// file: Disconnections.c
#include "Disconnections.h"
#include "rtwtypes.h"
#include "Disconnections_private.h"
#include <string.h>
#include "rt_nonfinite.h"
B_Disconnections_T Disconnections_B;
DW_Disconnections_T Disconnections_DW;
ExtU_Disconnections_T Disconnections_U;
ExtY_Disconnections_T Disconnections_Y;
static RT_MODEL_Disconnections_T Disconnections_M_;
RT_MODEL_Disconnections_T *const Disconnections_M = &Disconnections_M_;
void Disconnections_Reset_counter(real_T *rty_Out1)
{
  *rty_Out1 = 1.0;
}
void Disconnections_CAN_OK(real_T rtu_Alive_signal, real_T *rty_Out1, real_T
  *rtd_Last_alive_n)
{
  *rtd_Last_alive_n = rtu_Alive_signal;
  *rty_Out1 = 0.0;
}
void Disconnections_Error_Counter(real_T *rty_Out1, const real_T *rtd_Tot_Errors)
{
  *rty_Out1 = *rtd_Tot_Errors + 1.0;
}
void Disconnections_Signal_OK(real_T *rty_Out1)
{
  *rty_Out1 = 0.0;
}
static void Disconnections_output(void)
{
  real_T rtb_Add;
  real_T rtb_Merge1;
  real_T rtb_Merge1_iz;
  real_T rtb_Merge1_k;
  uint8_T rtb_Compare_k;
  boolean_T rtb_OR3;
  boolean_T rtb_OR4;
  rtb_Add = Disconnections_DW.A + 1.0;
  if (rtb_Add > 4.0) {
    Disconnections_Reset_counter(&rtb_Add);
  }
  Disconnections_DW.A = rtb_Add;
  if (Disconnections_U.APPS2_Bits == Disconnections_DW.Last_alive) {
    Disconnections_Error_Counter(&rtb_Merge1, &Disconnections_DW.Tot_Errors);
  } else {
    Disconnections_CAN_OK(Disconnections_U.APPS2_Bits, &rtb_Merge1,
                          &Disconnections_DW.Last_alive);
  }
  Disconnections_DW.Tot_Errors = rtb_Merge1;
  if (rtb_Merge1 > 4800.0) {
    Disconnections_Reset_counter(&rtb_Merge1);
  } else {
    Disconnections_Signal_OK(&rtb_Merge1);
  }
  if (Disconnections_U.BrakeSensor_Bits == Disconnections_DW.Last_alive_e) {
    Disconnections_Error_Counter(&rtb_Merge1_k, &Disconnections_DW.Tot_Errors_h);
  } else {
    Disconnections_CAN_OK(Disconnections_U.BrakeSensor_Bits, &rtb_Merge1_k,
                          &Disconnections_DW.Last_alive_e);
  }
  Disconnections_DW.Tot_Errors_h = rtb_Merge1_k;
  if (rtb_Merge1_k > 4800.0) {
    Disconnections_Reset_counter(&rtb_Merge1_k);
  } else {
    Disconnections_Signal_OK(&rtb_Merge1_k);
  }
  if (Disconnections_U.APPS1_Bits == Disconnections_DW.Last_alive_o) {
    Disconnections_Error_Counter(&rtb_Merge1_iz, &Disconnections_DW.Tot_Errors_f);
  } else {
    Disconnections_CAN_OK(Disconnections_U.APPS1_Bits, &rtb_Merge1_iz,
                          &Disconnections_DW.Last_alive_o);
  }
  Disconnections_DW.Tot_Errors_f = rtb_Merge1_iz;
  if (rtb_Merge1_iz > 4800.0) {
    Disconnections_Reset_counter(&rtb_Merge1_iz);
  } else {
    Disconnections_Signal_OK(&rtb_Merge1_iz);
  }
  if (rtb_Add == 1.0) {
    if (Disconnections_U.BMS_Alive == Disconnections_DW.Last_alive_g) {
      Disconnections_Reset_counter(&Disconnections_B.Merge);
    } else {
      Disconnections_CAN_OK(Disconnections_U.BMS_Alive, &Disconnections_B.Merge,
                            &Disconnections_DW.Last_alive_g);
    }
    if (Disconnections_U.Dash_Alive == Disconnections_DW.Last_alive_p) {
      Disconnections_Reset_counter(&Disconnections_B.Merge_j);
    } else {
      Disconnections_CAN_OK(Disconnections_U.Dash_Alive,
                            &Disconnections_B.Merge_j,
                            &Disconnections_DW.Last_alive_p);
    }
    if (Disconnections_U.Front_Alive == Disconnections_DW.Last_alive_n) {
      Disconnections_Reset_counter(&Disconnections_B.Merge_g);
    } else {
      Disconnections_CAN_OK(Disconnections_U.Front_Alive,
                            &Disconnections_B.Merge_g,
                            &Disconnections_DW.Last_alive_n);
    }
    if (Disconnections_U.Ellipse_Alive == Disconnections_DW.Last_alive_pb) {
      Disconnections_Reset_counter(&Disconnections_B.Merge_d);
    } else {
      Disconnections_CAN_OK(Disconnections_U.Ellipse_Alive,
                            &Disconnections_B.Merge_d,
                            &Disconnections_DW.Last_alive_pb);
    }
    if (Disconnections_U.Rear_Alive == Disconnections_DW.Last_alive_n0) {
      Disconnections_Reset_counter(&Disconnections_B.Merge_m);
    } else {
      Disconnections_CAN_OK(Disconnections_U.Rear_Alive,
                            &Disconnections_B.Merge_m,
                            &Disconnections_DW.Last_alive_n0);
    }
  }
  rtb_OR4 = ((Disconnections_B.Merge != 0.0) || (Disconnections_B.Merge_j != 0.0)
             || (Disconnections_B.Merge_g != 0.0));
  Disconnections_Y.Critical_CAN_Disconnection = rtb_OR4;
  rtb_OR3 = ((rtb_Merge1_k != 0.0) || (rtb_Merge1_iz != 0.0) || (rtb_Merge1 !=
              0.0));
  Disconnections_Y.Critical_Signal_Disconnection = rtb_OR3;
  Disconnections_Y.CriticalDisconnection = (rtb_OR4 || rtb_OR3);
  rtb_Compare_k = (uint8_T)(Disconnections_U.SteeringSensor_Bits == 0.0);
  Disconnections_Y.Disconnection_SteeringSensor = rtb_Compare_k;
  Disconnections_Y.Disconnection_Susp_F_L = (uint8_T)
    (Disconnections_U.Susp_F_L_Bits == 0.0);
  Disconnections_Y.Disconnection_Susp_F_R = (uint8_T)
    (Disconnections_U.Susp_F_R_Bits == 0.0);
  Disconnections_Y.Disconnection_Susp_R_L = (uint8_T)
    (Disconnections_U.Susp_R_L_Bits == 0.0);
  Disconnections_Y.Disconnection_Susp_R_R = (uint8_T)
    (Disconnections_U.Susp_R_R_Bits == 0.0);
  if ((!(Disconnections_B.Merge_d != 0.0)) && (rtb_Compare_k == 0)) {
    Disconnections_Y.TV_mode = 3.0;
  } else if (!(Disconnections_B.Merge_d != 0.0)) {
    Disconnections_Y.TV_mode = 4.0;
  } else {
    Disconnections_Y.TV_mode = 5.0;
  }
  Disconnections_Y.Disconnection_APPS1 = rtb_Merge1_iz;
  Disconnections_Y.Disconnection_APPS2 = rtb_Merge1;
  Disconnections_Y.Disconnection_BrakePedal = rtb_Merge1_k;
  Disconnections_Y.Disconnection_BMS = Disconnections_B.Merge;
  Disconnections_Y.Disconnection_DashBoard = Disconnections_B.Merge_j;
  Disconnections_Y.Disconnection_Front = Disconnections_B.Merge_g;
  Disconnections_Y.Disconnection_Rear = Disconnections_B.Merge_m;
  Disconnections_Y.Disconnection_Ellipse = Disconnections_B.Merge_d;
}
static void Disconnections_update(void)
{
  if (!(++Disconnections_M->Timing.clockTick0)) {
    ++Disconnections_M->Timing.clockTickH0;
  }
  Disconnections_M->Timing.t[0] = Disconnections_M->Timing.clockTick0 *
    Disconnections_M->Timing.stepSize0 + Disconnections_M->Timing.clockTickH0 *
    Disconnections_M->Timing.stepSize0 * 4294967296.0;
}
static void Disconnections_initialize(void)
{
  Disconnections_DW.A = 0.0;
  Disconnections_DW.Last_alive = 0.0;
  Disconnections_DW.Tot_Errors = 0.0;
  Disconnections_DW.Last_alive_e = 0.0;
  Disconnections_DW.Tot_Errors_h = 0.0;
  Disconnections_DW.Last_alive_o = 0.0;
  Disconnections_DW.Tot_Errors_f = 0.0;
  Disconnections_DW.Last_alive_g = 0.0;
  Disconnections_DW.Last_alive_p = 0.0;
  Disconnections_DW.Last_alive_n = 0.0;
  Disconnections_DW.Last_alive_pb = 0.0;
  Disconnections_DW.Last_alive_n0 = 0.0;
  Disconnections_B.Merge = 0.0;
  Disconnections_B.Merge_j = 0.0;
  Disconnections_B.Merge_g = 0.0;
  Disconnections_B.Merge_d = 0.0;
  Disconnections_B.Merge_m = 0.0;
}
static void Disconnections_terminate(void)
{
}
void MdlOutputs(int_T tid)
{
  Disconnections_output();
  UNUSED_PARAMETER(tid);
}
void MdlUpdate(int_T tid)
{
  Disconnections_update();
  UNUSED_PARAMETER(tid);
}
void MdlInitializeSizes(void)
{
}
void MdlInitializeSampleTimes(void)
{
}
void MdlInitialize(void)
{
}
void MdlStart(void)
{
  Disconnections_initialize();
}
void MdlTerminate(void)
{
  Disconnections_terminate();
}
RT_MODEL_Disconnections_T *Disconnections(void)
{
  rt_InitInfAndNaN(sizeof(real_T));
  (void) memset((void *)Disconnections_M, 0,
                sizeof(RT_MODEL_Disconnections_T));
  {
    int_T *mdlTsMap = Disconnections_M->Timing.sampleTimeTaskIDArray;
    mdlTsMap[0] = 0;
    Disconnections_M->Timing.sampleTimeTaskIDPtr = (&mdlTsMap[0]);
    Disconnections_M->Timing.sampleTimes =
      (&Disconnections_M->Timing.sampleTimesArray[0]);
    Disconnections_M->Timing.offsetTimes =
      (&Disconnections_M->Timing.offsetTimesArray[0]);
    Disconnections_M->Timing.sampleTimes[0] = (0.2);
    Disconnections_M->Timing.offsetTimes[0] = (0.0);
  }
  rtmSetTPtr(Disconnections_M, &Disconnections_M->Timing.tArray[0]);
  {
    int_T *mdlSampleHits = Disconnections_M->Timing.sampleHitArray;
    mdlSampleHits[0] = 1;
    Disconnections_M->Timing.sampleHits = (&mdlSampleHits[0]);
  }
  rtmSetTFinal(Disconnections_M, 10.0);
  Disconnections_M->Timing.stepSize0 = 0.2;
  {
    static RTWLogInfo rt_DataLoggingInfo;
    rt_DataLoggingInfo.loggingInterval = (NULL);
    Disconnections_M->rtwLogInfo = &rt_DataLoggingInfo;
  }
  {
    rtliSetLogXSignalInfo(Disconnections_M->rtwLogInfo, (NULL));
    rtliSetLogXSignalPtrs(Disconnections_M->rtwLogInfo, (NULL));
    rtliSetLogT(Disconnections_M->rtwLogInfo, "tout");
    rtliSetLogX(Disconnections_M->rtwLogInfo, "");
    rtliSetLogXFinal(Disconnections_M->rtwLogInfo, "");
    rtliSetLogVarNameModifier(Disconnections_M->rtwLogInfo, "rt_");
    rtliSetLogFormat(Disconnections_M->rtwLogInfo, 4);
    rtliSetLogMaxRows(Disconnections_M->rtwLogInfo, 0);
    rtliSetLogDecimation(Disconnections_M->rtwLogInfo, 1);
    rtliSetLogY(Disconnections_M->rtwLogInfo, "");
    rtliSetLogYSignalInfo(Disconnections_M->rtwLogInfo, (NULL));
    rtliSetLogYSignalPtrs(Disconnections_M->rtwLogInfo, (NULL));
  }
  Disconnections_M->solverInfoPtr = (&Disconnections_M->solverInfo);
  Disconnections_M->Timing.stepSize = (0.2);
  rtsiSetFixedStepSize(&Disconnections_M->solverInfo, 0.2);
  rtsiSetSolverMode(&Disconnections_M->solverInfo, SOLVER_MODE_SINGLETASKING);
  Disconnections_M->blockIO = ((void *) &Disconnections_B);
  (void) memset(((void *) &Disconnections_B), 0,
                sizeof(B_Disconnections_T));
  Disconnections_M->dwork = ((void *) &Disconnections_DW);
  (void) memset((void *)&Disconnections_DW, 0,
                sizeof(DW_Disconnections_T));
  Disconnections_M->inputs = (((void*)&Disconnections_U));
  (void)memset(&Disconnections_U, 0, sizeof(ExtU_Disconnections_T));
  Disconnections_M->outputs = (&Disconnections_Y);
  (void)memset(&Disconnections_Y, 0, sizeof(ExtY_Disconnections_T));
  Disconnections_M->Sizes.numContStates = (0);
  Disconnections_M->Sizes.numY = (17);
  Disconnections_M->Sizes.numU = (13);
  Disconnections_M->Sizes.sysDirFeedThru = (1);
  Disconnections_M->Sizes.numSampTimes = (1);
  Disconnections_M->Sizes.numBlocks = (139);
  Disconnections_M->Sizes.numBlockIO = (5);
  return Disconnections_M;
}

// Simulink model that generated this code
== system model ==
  BMS_Alive : Inport
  Dash_Alive : Inport
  Front_Alive : Inport
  Ellipse_Alive : Inport
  Rear_Alive : Inport
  APPS1_Bits : Inport
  APPS2_Bits : Inport
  BrakeSensor_Bits : Inport
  SteeringSensor_Bits : Inport
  Susp_F_L_Bits : Inport
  Susp_F_R_Bits : Inport
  Susp_R_L_Bits : Inport
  Susp_R_R_Bits : Inport
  Critical_CAN_Disconnection : Outport  <- 1: OR4
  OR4 : Logic  Operator=OR  Inputs=3  <- 1: Subsystem#1, 2: Subsystem#1/2, 3: Subsystem#1/3
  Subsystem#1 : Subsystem  <- 1: BMS_Alive, 2: Dash_Alive, 3: Front_Alive, 4: Ellipse_Alive, 5: Rear_Alive, Action: If#1
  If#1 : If  IfExpression=u1 == 1  <- 1: Merge#1
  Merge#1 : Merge  <- 1: Reset_counter, 2: Subsystem#2
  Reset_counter : Subsystem  <- Action: If#2
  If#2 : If  IfExpression=u1 > u2  <- 1: Add, 2: Constant#1
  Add : Sum  <- 1: DataStoreRead#1, 2: Constant#2
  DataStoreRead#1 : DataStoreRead  Indices=1
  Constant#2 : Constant
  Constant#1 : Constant  Value=4
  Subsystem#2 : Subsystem  <- 1: Add, Action: If#2/2
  Critical_Signal_Disconnection : Outport  <- 1: OR3
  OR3 : Logic  Operator=OR  Inputs=3  <- 1: Merge1, 2: Merge#2, 3: Merge#3
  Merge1 : Merge  <- 1: Subsystem#3, 2: Signal_OK
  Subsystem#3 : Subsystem  <- Action: If#3
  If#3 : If  IfExpression=u1>u2  <- 1: Merge, 2: Constant#3
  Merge : Merge  <- 1: Error_Counter, 2: CAN_OK
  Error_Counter : Subsystem  <- Action: If#4
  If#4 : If  IfExpression=u1==u2  <- 1: BrakeSensor_Bits, 2: DataStoreRead#2
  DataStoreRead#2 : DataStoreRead  DataStoreName=Last_alive  Indices=1
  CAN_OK : Subsystem  <- 1: BrakeSensor_Bits, Action: If#4/2
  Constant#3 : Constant  Value=4800
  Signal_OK : Subsystem  <- Action: If#3/2
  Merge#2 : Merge  <- 1: Subsystem#4, 2: Subsystem#5
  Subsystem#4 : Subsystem  <- Action: If#5
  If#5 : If  IfExpression=u1>u2  <- 1: Merge#4, 2: Constant#3
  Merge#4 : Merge  <- 1: Subsystem#6, 2: Subsystem#7
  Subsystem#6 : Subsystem  <- Action: If#6
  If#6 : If  IfExpression=u1==u2  <- 1: APPS1_Bits, 2: DataStoreRead#3
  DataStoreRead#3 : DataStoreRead  DataStoreName=Last_alive  Indices=1
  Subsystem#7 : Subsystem  <- 1: APPS1_Bits, Action: If#6/2
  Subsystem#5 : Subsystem  <- Action: If#5/2
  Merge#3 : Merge  <- 1: Subsystem#8, 2: Subsystem#9
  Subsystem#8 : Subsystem  <- Action: If#7
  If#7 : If  IfExpression=u1>u2  <- 1: Merge#5, 2: Constant#3
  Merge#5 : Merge  <- 1: Subsystem#10, 2: Subsystem#11
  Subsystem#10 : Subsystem  <- Action: If#8
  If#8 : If  IfExpression=u1==u2  <- 1: APPS2_Bits, 2: DataStoreRead#4
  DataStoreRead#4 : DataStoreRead  DataStoreName=Last_alive  Indices=1
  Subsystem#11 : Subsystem  <- 1: APPS2_Bits, Action: If#8/2
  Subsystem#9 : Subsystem  <- Action: If#7/2
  CriticalDisconnection : Outport  <- 1: Logic#1
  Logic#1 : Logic  Operator=OR  <- 1: OR4, 2: OR3
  Disconnection_SteeringSensor : Outport  <- 1: CompareToZero#1
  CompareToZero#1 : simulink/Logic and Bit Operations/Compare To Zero  relop===  <- 1: SteeringSensor_Bits
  Disconnection_Susp_F_L : Outport  <- 1: CompareToZero#2
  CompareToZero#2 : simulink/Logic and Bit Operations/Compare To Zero  relop===  <- 1: Susp_F_L_Bits
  Disconnection_Susp_F_R : Outport  <- 1: CompareToZero#3
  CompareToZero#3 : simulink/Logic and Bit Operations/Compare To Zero  relop===  <- 1: Susp_F_R_Bits
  Disconnection_Susp_R_L : Outport  <- 1: CompareToZero#4
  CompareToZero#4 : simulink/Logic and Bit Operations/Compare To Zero  relop===  <- 1: Susp_R_L_Bits
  Disconnection_Susp_R_R : Outport  <- 1: CompareToZero#5
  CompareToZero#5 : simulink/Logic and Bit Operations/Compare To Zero  relop===  <- 1: Susp_R_R_Bits
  TV_mode : Outport  <- 1: Merge#6
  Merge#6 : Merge  <- 1: Subsystem#12, 2: Subsystem#13
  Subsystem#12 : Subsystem  <- Action: If#9
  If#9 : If  IfExpression=u1 ==1  <- 1: Logic#2
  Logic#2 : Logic  Operator=NOT  <- 1: Logic#3
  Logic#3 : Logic  Operator=OR  <- 1: Subsystem#1/4, 2: CompareToZero#1
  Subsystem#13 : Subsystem  <- 1: Merge#7, Action: If#9/2
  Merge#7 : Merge  <- 1: Subsystem#14, 2: Subsystem#15
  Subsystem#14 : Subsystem  <- Action: If#10
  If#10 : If  IfExpression=u1 ==1  <- 1: Logic#4
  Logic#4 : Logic  Operator=NOT  <- 1: Subsystem#1/4
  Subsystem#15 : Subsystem  <- Action: If#10/2
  Disconnection_APPS1 : Outport  <- 1: Merge#2
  Disconnection_APPS2 : Outport  <- 1: Merge#3
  Disconnection_BrakePedal : Outport  <- 1: Merge1
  Disconnection_BMS : Outport  <- 1: Subsystem#1
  Disconnection_DashBoard : Outport  <- 1: Subsystem#1/2
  Disconnection_Front : Outport  <- 1: Subsystem#1/3
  Disconnection_Rear : Outport  <- 1: Subsystem#1/5
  Disconnection_Ellipse : Outport  <- 1: Subsystem#1/4
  DataStoreWrite#1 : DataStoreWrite  Indices=1  <- 1: Merge#1
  DataStoreWrite#2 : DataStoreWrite  DataStoreName=Tot_Errors  Indices=1  <- 1: Merge#5
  DataStoreWrite#3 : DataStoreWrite  DataStoreName=Tot_Errors  Indices=1  <- 1: Merge
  DataStoreWrite#4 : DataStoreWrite  DataStoreName=Tot_Errors  Indices=1  <- 1: Merge#4
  DataStoreMemory#1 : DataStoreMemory
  DataStoreMemory#2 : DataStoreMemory  DataStoreName=Last_alive
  DataStoreMemory#3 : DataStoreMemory  DataStoreName=Last_alive
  DataStoreMemory#4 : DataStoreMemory  DataStoreName=Last_alive
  DataStoreMemory#5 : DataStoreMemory  DataStoreName=Tot_Errors
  DataStoreMemory#6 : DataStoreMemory  DataStoreName=Tot_Errors
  DataStoreMemory#7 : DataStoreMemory  DataStoreName=Tot_Errors
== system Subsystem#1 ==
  Inport#1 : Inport
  Inport#2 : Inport
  Inport#3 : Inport
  Inport#4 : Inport
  Inport#5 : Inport
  ActionPort#1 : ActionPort
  Outport#1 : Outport  <- 1: Merge#8
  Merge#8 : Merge  <- 1: Subsystem#16, 2: Subsystem#17
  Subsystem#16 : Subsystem  <- Action: If#11
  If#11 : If  IfExpression=u1==u2  <- 1: Inport#1, 2: DataStoreRead#5
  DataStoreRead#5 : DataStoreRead  DataStoreName=Last_alive  Indices=1
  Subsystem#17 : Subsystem  <- 1: Inport#1, Action: If#11/2
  Outport#2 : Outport  <- 1: Merge#9
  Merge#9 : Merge  <- 1: Subsystem#18, 2: Subsystem#19
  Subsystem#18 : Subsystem  <- Action: If#12
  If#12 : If  IfExpression=u1==u2  <- 1: Inport#2, 2: DataStoreRead#6
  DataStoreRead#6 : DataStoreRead  DataStoreName=Last_alive  Indices=1
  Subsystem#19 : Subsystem  <- 1: Inport#2, Action: If#12/2
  Outport#3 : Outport  <- 1: Merge#10
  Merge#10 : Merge  <- 1: Subsystem#20, 2: Subsystem#21
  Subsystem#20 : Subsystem  <- Action: If#13
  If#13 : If  IfExpression=u1==u2  <- 1: Inport#3, 2: DataStoreRead#7
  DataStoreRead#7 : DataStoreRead  DataStoreName=Last_alive  Indices=1
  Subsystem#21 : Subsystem  <- 1: Inport#3, Action: If#13/2
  Outport#4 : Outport  <- 1: Merge#11
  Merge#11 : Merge  <- 1: Subsystem#22, 2: Subsystem#23
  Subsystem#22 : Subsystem  <- Action: If#14
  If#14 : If  IfExpression=u1==u2  <- 1: Inport#4, 2: DataStoreRead#8
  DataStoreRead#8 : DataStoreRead  DataStoreName=Last_alive  Indices=1
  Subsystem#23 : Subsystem  <- 1: Inport#4, Action: If#14/2
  Outport#5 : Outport  <- 1: Merge#12
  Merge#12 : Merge  <- 1: Subsystem#24, 2: Subsystem#25
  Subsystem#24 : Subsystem  <- Action: If#15
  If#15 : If  IfExpression=u1==u2  <- 1: Inport#5, 2: DataStoreRead#9
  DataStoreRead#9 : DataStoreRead  DataStoreName=Last_alive  Indices=1
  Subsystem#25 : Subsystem  <- 1: Inport#5, Action: If#15/2
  DataStoreMemory#8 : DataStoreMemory  DataStoreName=Last_alive
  DataStoreMemory#9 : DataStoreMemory  DataStoreName=Last_alive
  DataStoreMemory#10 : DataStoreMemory  DataStoreName=Last_alive
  DataStoreMemory#11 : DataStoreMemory  DataStoreName=Last_alive
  DataStoreMemory#12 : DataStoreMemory  DataStoreName=Last_alive
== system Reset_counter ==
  ActionPort#2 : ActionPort
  Out1 : Outport  <- 1: Constant#4
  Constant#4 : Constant
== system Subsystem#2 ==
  Inport#6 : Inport
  ActionPort#3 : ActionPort
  Outport#6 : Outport  <- 1: Inport#6
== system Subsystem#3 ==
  ActionPort#4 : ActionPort
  Outport#7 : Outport  <- 1: Constant#5
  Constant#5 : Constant
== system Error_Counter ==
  ActionPort#5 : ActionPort
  Outport#8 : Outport  <- 1: Sum#1
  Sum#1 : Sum  <- 1: DataStoreRead#10, 2: Constant#6
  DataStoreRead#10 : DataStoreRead  DataStoreName=Tot_Errors  Indices=1
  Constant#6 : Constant
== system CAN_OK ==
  Alive_signal : Inport
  ActionPort#6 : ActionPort
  Outport#9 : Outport  <- 1: Constant#7
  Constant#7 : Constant  Value=0
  DataStoreWrite#5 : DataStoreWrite  DataStoreName=Last_alive  Indices=1  <- 1: Alive_signal
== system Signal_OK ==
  ActionPort#7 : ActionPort
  Outport#10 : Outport  <- 1: Constant#8
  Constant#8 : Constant  Value=0
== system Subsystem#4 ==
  ActionPort#8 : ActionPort
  Outport#11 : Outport  <- 1: Constant#9
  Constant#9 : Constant
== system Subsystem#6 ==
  ActionPort#9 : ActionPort
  Outport#12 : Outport  <- 1: Sum#2
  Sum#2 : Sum  <- 1: DataStoreRead#11, 2: Constant#10
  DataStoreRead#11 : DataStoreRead  DataStoreName=Tot_Errors  Indices=1
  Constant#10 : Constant
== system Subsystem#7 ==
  Inport#7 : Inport
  ActionPort#10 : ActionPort
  Outport#13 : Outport  <- 1: Constant#11
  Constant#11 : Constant  Value=0
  DataStoreWrite#6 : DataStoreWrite  DataStoreName=Last_alive  Indices=1  <- 1: Inport#7
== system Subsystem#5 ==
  ActionPort#11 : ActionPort
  Outport#14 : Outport  <- 1: Constant#12
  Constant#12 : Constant  Value=0
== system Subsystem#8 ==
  ActionPort#12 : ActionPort
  Outport#15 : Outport  <- 1: Constant#13
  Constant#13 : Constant
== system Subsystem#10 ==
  ActionPort#13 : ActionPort
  Outport#16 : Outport  <- 1: Sum#3
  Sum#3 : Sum  <- 1: DataStoreRead#12, 2: Constant#14
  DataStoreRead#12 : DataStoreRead  DataStoreName=Tot_Errors  Indices=1
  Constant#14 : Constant
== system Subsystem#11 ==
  Inport#8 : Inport
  ActionPort#14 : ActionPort
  Outport#17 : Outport  <- 1: Constant#15
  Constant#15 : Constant  Value=0
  DataStoreWrite#7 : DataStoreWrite  DataStoreName=Last_alive  Indices=1  <- 1: Inport#8
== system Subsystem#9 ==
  ActionPort#15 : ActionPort
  Outport#18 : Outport  <- 1: Constant#16
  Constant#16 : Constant  Value=0
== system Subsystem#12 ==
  ActionPort#16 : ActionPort
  Outport#19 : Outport  <- 1: Constant#17
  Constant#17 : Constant  Value=3
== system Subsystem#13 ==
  Inport#9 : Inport
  ActionPort#17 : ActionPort
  Outport#20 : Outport  <- 1: Inport#9
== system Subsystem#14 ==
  ActionPort#18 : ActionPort
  Outport#21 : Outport  <- 1: Constant#18
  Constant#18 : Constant  Value=4
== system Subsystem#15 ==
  ActionPort#19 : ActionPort
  Outport#22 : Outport  <- 1: Constant#19
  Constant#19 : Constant  Value=5
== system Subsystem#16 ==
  ActionPort#20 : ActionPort
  Outport#23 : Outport  <- 1: Constant#20
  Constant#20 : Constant
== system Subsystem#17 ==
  Inport#10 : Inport
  ActionPort#21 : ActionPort
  Outport#24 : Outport  <- 1: Constant#21
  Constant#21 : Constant  Value=0
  DataStoreWrite#8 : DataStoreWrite  DataStoreName=Last_alive  Indices=1  <- 1: Inport#10
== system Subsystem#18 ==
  ActionPort#22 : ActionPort
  Outport#25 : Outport  <- 1: Constant#22
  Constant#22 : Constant
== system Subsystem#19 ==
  Inport#11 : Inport
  ActionPort#23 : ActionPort
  Outport#26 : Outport  <- 1: Constant#23
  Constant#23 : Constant  Value=0
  DataStoreWrite#9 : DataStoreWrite  DataStoreName=Last_alive  Indices=1  <- 1: Inport#11
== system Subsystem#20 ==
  ActionPort#24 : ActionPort
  Outport#27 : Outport  <- 1: Constant#24
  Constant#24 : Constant
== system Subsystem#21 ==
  Inport#12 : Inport
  ActionPort#25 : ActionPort
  Outport#28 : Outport  <- 1: Constant#25
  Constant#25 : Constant  Value=0
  DataStoreWrite#10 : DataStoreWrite  DataStoreName=Last_alive  Indices=1  <- 1: Inport#12
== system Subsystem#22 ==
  ActionPort#26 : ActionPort
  Outport#29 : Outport  <- 1: Constant#26
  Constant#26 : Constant
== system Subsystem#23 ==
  Inport#13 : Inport
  ActionPort#27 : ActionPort
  Outport#30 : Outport  <- 1: Constant#27
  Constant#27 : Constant  Value=0
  DataStoreWrite#11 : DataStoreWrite  DataStoreName=Last_alive  Indices=1  <- 1: Inport#13
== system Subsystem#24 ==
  ActionPort#28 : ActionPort
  Outport#31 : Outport  <- 1: Constant#28
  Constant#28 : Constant
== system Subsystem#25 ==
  Inport#14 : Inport
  ActionPort#29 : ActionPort
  Outport#32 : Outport  <- 1: Constant#29
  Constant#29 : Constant  Value=0
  DataStoreWrite#12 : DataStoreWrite  DataStoreName=Last_alive  Indices=1  <- 1: Inport#14
